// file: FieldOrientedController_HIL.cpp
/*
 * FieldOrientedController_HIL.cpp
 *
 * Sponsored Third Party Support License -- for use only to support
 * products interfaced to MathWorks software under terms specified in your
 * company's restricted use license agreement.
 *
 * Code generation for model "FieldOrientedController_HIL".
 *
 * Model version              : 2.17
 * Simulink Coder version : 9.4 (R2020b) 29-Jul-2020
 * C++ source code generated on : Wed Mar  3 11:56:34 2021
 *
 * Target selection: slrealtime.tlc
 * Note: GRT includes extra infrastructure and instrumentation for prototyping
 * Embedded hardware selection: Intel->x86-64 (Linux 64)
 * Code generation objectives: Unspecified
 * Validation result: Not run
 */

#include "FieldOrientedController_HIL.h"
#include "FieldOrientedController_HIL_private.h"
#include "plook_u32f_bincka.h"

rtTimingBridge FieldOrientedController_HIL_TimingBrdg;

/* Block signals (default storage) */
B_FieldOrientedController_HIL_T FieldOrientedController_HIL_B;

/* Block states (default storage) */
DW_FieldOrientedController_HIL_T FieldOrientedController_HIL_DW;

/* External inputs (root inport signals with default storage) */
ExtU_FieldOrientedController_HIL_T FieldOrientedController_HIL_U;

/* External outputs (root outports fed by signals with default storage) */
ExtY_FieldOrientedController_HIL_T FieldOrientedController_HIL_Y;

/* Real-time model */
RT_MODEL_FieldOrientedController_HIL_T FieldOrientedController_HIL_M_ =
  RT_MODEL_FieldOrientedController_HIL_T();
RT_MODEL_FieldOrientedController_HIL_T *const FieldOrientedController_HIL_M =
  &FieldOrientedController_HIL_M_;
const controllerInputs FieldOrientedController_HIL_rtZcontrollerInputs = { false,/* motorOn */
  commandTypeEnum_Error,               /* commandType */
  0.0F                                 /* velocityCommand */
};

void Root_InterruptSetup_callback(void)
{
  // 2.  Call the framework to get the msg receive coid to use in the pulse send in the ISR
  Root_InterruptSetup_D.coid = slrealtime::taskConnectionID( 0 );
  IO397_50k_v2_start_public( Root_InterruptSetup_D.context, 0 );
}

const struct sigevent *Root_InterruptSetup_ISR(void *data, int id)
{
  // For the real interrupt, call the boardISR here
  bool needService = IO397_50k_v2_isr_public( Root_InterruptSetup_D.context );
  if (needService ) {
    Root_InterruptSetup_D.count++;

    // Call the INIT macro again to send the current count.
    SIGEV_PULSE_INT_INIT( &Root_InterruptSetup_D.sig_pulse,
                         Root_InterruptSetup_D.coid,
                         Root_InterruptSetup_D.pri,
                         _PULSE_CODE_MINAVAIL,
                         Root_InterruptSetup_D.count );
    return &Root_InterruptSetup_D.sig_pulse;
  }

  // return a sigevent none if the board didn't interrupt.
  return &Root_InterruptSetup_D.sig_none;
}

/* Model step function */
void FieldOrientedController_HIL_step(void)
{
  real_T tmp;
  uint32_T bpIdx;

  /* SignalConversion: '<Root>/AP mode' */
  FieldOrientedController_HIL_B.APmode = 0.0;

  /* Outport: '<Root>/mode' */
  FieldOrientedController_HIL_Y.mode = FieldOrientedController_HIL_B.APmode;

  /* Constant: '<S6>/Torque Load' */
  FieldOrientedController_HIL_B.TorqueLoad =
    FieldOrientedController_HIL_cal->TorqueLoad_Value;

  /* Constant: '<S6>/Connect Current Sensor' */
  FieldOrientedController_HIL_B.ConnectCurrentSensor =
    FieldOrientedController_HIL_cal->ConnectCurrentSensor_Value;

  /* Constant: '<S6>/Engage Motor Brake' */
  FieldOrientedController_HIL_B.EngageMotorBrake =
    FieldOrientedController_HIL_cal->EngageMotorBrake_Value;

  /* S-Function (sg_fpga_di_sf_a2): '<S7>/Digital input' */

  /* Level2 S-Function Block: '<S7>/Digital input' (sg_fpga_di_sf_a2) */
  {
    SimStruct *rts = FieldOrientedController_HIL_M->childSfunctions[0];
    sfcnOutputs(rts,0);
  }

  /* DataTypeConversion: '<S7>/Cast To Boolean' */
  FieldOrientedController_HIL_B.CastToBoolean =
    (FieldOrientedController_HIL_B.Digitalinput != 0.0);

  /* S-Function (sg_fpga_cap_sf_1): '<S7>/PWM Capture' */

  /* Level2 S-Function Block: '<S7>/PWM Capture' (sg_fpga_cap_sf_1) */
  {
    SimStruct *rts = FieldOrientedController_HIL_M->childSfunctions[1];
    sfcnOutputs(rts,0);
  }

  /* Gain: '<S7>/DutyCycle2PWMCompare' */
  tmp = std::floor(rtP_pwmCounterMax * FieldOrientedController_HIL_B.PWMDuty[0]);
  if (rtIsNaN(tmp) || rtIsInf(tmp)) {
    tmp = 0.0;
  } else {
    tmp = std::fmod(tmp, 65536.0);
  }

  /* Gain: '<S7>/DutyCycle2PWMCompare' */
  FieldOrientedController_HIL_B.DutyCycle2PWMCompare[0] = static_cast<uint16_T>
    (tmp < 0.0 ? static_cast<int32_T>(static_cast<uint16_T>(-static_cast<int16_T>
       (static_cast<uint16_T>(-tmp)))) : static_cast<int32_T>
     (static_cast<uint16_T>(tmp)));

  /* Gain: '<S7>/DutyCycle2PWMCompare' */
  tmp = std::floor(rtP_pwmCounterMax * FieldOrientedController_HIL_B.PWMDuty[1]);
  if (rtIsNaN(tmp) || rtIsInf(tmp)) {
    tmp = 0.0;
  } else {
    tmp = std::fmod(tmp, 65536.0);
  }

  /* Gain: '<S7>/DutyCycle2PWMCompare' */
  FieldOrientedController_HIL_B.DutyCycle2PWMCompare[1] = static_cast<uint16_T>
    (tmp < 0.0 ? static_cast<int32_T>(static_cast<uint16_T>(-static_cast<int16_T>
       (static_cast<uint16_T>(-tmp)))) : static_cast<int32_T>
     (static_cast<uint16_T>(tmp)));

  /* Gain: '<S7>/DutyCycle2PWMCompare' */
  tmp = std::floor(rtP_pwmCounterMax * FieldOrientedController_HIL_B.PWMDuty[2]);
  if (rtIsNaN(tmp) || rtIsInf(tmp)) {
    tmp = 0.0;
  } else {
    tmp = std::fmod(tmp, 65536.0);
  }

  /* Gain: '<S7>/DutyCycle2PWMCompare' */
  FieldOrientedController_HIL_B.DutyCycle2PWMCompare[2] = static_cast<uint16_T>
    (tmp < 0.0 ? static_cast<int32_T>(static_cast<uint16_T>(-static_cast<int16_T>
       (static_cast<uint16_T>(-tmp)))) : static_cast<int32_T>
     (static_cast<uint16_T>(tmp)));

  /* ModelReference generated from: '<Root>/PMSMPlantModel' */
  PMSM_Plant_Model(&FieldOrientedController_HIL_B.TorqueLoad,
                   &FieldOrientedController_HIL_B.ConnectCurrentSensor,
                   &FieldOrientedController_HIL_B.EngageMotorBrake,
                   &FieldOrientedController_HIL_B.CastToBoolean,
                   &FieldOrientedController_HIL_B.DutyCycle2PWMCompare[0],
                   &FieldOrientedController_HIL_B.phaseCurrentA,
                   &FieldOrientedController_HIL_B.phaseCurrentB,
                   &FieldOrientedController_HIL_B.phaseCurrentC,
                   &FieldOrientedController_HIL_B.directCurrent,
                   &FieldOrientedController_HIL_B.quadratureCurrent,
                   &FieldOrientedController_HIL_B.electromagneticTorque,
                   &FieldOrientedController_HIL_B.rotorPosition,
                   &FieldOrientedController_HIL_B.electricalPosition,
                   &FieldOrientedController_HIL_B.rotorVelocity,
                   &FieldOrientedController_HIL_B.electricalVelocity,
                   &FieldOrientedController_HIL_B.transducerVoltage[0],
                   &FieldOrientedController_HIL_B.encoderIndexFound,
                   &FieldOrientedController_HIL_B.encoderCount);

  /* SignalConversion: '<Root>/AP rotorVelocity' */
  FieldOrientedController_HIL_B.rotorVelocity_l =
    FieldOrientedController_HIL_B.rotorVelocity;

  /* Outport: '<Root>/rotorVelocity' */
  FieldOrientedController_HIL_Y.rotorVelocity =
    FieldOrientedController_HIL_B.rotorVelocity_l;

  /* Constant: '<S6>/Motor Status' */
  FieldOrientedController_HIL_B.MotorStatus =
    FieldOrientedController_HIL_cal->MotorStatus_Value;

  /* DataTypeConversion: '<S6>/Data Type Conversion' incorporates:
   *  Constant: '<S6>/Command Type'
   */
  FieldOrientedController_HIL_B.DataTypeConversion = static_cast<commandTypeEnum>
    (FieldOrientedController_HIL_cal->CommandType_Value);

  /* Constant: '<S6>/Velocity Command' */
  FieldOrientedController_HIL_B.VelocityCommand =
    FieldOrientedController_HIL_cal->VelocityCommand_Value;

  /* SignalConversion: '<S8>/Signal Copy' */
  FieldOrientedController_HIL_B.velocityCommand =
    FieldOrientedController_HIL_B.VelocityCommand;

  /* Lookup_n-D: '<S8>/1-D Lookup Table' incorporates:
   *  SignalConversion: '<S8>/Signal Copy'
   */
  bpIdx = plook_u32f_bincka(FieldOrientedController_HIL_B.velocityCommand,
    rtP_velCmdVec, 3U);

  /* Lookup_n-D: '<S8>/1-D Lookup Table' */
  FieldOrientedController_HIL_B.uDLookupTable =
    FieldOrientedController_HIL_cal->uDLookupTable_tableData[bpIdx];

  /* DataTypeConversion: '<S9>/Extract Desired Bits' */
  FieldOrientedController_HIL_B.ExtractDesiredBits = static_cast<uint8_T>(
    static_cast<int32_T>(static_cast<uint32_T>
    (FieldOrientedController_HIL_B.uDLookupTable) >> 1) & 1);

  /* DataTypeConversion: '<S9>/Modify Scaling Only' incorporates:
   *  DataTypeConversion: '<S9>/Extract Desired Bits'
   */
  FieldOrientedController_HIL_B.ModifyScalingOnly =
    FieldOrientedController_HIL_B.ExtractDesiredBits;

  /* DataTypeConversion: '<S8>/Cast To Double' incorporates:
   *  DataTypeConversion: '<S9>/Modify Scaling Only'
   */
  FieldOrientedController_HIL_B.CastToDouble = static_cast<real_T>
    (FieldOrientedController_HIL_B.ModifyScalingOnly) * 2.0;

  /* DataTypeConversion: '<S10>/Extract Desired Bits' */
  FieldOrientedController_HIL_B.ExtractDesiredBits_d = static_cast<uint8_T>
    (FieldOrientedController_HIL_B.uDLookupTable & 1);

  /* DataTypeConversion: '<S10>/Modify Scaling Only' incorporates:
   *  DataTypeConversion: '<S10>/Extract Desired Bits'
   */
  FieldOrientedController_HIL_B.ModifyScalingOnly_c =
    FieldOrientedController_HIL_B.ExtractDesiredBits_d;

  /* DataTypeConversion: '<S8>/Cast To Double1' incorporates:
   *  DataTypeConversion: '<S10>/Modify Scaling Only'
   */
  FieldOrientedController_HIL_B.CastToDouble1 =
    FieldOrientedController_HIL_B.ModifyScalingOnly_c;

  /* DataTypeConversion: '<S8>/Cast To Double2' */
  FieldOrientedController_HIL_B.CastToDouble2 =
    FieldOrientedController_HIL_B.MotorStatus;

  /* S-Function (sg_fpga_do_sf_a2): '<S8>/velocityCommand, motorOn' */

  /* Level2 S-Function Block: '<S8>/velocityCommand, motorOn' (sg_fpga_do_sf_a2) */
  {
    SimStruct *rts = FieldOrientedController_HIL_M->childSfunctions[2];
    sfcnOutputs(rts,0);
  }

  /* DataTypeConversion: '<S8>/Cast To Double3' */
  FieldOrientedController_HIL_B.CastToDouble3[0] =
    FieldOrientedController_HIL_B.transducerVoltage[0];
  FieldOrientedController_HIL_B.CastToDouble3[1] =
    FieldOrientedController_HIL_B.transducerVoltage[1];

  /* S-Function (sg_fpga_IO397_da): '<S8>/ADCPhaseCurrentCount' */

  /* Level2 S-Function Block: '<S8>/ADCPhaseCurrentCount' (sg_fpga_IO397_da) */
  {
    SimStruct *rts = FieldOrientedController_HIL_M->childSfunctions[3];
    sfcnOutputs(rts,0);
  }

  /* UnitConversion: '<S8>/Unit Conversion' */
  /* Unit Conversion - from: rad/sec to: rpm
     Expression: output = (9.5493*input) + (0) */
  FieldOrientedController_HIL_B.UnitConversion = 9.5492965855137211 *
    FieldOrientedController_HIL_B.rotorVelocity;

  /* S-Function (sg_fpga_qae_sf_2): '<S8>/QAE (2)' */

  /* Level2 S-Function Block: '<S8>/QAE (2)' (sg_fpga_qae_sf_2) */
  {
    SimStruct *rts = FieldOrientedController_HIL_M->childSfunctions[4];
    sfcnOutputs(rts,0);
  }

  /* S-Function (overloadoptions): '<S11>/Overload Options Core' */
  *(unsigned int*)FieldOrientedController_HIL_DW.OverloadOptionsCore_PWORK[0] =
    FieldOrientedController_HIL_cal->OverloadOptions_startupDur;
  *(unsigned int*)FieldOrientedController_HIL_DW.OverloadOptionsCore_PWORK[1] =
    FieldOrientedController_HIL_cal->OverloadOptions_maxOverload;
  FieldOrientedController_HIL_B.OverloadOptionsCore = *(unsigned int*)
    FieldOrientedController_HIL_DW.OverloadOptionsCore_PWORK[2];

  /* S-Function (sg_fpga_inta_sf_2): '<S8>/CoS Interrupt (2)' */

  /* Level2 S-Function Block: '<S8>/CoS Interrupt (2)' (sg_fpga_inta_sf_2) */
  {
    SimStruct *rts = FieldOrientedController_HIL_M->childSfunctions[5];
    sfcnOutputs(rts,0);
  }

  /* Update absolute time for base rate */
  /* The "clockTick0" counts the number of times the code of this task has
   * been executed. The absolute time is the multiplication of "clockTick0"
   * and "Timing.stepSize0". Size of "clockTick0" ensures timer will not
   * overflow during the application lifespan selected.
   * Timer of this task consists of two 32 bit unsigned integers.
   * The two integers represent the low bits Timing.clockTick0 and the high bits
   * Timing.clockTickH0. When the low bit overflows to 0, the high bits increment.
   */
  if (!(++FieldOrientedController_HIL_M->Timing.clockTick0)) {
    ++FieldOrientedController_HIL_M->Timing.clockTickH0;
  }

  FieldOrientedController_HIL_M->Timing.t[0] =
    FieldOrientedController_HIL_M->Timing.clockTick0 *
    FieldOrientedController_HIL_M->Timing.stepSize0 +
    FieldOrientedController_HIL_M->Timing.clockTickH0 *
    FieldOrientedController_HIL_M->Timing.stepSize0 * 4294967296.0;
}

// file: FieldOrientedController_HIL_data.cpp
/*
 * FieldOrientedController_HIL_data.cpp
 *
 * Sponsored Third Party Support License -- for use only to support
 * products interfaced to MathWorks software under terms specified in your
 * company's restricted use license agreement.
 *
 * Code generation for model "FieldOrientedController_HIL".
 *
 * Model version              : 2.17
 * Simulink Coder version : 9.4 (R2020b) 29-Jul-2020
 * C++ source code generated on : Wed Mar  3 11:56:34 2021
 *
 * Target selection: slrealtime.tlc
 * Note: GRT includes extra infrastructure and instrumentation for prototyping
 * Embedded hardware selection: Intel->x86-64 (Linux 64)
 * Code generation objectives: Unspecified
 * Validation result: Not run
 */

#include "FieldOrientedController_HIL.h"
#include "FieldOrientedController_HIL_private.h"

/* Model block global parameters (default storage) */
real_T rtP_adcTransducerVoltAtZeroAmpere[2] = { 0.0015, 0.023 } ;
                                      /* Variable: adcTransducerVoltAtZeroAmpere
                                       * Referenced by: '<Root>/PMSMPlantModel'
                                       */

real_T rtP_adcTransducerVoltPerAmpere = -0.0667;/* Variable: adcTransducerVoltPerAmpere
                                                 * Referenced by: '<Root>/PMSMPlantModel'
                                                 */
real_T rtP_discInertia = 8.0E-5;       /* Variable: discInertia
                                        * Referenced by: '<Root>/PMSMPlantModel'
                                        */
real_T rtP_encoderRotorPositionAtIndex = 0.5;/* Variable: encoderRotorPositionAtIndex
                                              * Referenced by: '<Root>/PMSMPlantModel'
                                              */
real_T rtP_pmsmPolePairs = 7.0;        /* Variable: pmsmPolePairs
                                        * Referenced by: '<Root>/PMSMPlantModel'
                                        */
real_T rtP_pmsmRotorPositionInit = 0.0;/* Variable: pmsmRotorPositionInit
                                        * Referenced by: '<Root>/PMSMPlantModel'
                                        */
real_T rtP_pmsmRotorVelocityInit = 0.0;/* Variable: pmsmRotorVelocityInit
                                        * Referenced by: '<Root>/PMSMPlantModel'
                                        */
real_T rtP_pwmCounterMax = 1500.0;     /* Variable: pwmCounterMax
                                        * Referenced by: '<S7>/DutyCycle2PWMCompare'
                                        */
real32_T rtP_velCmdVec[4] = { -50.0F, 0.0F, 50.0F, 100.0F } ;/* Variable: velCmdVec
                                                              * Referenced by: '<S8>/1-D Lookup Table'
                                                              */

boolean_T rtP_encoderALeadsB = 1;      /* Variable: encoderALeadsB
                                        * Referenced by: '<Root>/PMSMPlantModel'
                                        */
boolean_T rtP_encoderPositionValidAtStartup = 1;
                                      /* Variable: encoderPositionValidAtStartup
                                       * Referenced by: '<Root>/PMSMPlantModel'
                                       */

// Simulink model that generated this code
simulink model "FieldOrientedController_HIL"  (R2020b)
settings: configuration reference "SLRT_HIL" (kept outside this file)
undefined symbols (not defined in the file): encoderNumberOfSlits, idxVec, IO397, modeSchedulerEnum, pwmCounterMax, sampleTimeCurrentControl, velCmdVec
libraries: utils_lib x2, speedgoatlib_fpga_dio x2, simulink x2, SignalEditorBlockLib x1, speedgoatlib_interrupt x1, speedgoatlib_fpga_pwm x1, speedgoatlib_fpga_analog_io x1, speedgoatlib_fpga_inta x1, slrealtimetgmanagement x1, speedgoatlib_fpga_quadrature x1, speedgoatlib_fpga x1

== system FieldOrientedController_HIL ==
  note: Electric Motor Control
      | Reference application model
      | © 2007 - 2020 Speedgoat GmbH
  physicalInputs : Inport  OutDataTypeStr=Bus: physicalInputs
  controllerInputs : Inport  Port=2  OutDataTypeStr=Bus: controllerInputs
  ADC : utils_lib/ADC  SystemSampleTime=-1  VariantActivationTime=update diagram  Latency=0  AutoFrameSizeCalculation=off
  AP mode : SignalConversion  OverrideOpt=off
  AP rotorVelocity : SignalConversion  OverrideOpt=off
  Bus Selector : BusSelector  OutputSignals=rotorVelocity
  DAC : utils_lib/DAC  SystemSampleTime=-1  VariantActivationTime=update diagram  Latency=0  AutoFrameSizeCalculation=off
  Inputs : Subsystem  Variant=on  VariantControlMode=label  VariantControl=Choice  LabelModeActiveChoice=dashboardInput
  Interrupt Setup : speedgoatlib_interrupt/Interrupt Setup  parModuleTrigger=on  parPollingMode=off  parPriorityConf=High  parPriority=241  confStartFcn=IO397_50k_v2_start_public  confStopFcn=IO397_50k_v2_stop_public  confIsrFcn=IO397_50k_v2_isr_public  confMapFcn=IO397_50k_v2_map_public  confHookFile=io397_50k_v2_int_hooks.c  confIrqNr=-1  confIsMdlTrig=on  confIsPolling=off  confPriority=254  confModID=1  confSelectedInt=Speedgoat IO397-50k v2 interrupt  confSelectedId=1
  PMSMPlantModel : ModelReference  ModelNameDialog=PMSM_Plant_Model  SimulationMode=Normal  ModelReferenceVersion=2.0
  Signal Copy : SignalConversion  OverrideOpt=off
  Signal Copy1 : SignalConversion  OverrideOpt=off
  TIC2000 : Subsystem  VariantControl=demoMode == 3
  UserInterface : Subsystem
  mode : Outport
  rotorVelocity : Outport  Port=2
  tag scope: rotorVelocity=global
  wires:
  ADC/2 -> TIC2000/2(controllerFeedback)
  PMSMPlantModel/1 -> Bus Selector/1  "motorMeasurements"
  ADC/1 -> TIC2000/1(controllerInputs)
  TIC2000/2(" controllerCommands") -> DAC/1  "motorCommands"
  DAC/1 -> PMSMPlantModel/2
  Bus Selector/1 -> [rotorVelocity], AP rotorVelocity/1  "<rotorVelocity>"
  Inputs/2(controllerInputs) -> ADC/1  "controllerInputs"
  physicalInputs/1 -> Signal Copy/1
  controllerInputs/1 -> Signal Copy1/1
  Inputs/1(physicalInputs) -> PMSMPlantModel/1  "physicalInputs"
  AP rotorVelocity/1 -> rotorVelocity/1  "rotorVelocity"
  TIC2000/1(mode) -> AP mode/1
  AP mode/1 -> mode/1
  PMSMPlantModel/2 -> ADC/2  "controllerFeedback"
  Signal Copy/1 -> Inputs/1(physicalInputs_in)
  Signal Copy1/1 -> Inputs/2(controllerInputs_in)

== system FieldOrientedController_HIL/Inputs ==
  physicalInputs_in : Inport  OutDataTypeStr=Bus: physicalInputs
  controllerInputs_in : Inport  Port=2  OutDataTypeStr=Bus: controllerInputs
  Dashboard : Subsystem  VariantControl=dashboardInput
  Harness : Subsystem  VariantControl=harnessInput
  Signal Builder : Subsystem  VariantControl=sigBuilderInput
  physicalInputs : Outport  OutDataTypeStr=Bus: physicalInputs
  controllerInputs : Outport  Port=2  OutDataTypeStr=Bus: controllerInputs

== system FieldOrientedController_HIL/TIC2000 ==
  note: TI C2000 Controller
  controllerInputs : Inport
  controllerFeedback : Inport  Port=2
  Speedgoat_inputs : Subsystem
  Speedgoat_outputs : Subsystem
  mode : Outport
  " controllerCommands" : Outport  Port=2  VectorParamsAs1DForOutWhenUnconnected=off
  wires:
  Speedgoat_inputs/2(commands) -> " controllerCommands"/1
  Speedgoat_inputs/1(mode) -> mode/1
  controllerFeedback/1 -> Speedgoat_outputs/2(feedback)
  controllerInputs/1 -> Speedgoat_outputs/1(inputs)

== system FieldOrientedController_HIL/UserInterface ==
  Dashboard Scope : DashboardScope  TimeSpan=10  Ymin=-200  Ymax=200  ScaleAtStop=off
  Half Gauge : SemiCircularGaugeBlock  ScaleMin=-200  ScaleMax=200
  Rotary Switch : RotarySwitchBlock
  Toggle Switch : ToggleSwitchBlock

== system FieldOrientedController_HIL/Inputs/Dashboard ==
  Command Type : Constant  Value=3  OutDataTypeStr=uint8
  Connect Current Sensor : Constant  OutDataTypeStr=boolean
  Data Type Conversion : DataTypeConversion  OutDataTypeStr=Enum: commandTypeEnum
  Engage Motor Brake : Constant  Value=0  OutDataTypeStr=boolean
  Motor Status : Constant  OutDataTypeStr=boolean
  Torque Load : Constant  Value=0  OutDataTypeStr=Inherit: Inherit via back propagation
  Velocity Command : Constant  Value=100  OutDataTypeStr=Inherit: Inherit via back propagation
  Bus Element Out : Outport  PortName=physicalInputs  Element=torqueLoad
  Bus Element Out1 : Outport  PortName=physicalInputs  Element=connectCurrentSensor
  Bus Element Out2 : Outport  PortName=physicalInputs  Element=motorBrake
  Bus Element Out3 : Outport  Port=2  PortName=controllerInputs  Element=motorOn
  Bus Element Out4 : Outport  Port=2  PortName=controllerInputs  Element=commandType
  Bus Element Out5 : Outport  Port=2  PortName=controllerInputs  Element=velocityCommand
  wires:
  Engage Motor Brake/1 -> Bus Element Out2/1
  Data Type Conversion/1 -> Bus Element Out4/1
  Connect Current Sensor/1 -> Bus Element Out1/1
  Torque Load/1 -> Bus Element Out/1
  Velocity Command/1 -> Bus Element Out5/1
  Command Type/1 -> Data Type Conversion/1
  Motor Status/1 -> Bus Element Out3/1

== system FieldOrientedController_HIL/Inputs/Harness ==
  physicalInputs_in : Inport  OutDataTypeStr=Bus: physicalInputs
  controllerInputs_in : Inport  Port=2  OutDataTypeStr=Bus: controllerInputs
  physicalInputs : Outport  OutDataTypeStr=Bus: physicalInputs
  controllerInputs : Outport  Port=2  OutDataTypeStr=Bus: controllerInputs
  wires:
  physicalInputs_in/1 -> physicalInputs/1
  controllerInputs_in/1 -> controllerInputs/1

== system FieldOrientedController_HIL/Inputs/Signal Builder ==
  Signal Editor : SignalEditorBlockLib/Signal Editor  FileName=systemInputs.mat  ActiveScenario=doubleStepPosNegClosedLoop  ActiveSignal=controlInputs  IsBus=on  OutputBusObjectStr=Bus: controllerInputs  SampleTime=-1  Interpolate=off  ZeroCross=off  OutputAfterFinalValue=Holding final value  Unit=inherit  PreserveSignalName=on
  physicalInputs : Outport  OutDataTypeStr=Bus: physicalInputs
  controllerInputs : Outport  Port=2  OutDataTypeStr=Bus: controllerInputs
  wires:
  Signal Editor/1 -> physicalInputs/1
  Signal Editor/2 -> controllerInputs/1

== system FieldOrientedController_HIL/TIC2000/Speedgoat_inputs ==
  Cast To Boolean : DataTypeConversion  OutDataTypeStr=boolean
  Constant : Constant  Commented=on  Value=modeSchedulerEnum(0)
  Digital input : speedgoatlib_fpga_dio/Digital input  id=1  chan=[2]  ts=sampleTimeCurrentControl  pciSlot=-1  board=IO397-50k  vectorizeOutput=off
  DutyCycle2PWMCompare : Gain  Gain=pwmCounterMax  OutDataTypeStr=Inherit: Inherit via back propagation
  PWM Capture : speedgoatlib_fpga_pwm/PWM Capture  id=1  chan=[1 2 3]  ts=sampleTimeCurrentControl  pciSlot=-1  board=IO397-50k  captureMode=High transitions triggered  captureTimeout=0  bit_width_cap=24  showHighDuration=off  showLowDuration=off  showPeriod=off  showDC16=on  showDC8=off  showTOn=off  showTOff=off  showValidData=off
  mode : Outport
  Bus Element Out : Outport  Port=2  PortName=commands  Element=inverterEnable
  Bus Element Out1 : Outport  Port=2  PortName=commands  Element=pwmCompare
  wires:
  PWM Capture/1 -> DutyCycle2PWMCompare/1  "PWMDuty"
  Digital input/1 -> Cast To Boolean/1
  DutyCycle2PWMCompare/1 -> Bus Element Out1/1
  Cast To Boolean/1 -> Bus Element Out/1
  Constant/1 -> mode/1

== system FieldOrientedController_HIL/TIC2000/Speedgoat_outputs ==
  Bus Element In1 : Inport  PortName=inputs  Element=motorOn
  Bus Element In : Inport  PortName=inputs  Element=velocityCommand
  Bus Element In2 : Inport  Port=2  PortName=feedback  Element=transducerVoltage
  1-D Lookup Table : Lookup_n-D  NumberOfTableDimensions=1  BreakpointsForDimension1=velCmdVec  Table=idxVec  InterpMethod=Flat  InternalRulePriority=Speed  OutDataTypeStr=uint8  RndMeth=Simplest  InputSameDT=on
  ADCPhaseCurrentCount : speedgoatlib_fpga_analog_io/IO397 Analog Output  id=1  chan=1:2  initVal=0  resetVal=1  ts=-1  pciSlot=-1  board=IO397-50k  span=+-5 V
  Cast To Double{,1..3} (4 alike) : DataTypeConversion  OutDataTypeStr=double
  CoS Interrupt (2) : speedgoatlib_fpga_inta/CoS Interrupt (2)  id=1  channel=[1]  pciSlot=-1  ts=-1  board=IO397-50k  fpga_frequency=0  int_source=internally generated  mode=0  debounce=0  delay=0  ad_settings=off  division=0  multiplication=0  gap=1e-3  int_freq=1/sampleTimeCurrentControl  freq_2_time=2.50000e-04  event=off  timestamp=off  flag=off
  Demux : Demux  Outputs=2
  Extract Bits : simulink/Logic and Bit Operations/Extract Bits  bitsToExtract=Range of bits  numBits=8  bitIdxRange=1  outScalingMode=Preserve fixed-point scaling
  Extract Bits1 : simulink/Logic and Bit Operations/Extract Bits  bitsToExtract=Range of bits  numBits=8  bitIdxRange=0  outScalingMode=Preserve fixed-point scaling
  Overload Options : slrealtimetgmanagement/Overload Options  startupDur=10  startupDurSrc=Tunable Parameter  maxOverload=10  maxOverloadSrc=Tunable Parameter  TETFlag=off
  QAE (2) : speedgoatlib_fpga_quadrature/QAE (2)  id=1  channel=1  ts=-1  pciSlot=-1  board=IO397-50k  numSeg=encoderNumberOfSlits*2  phaseAngle=90  initSpeed=0  initPos=pmsmRotorPositionInit  freeWheel=on  showInputSpeed=on  showInputPosition=off  showOutputPosition=off
  Setup : speedgoatlib_fpga/Setup/Setup  board=IO397-50k  id=1  device_id=1  frontIO=None  rearIO=None  bitstreamFile=speedgoat_IO397_50k_CI_02168  rev=1.0  timestamp_string=26/08/20 11:01:36  fpgaFreq=75 MHz  fpgaTick=13.33 ns  ProgSpiFlash=off  ProgBPIFlash=off  pciSlot=-1  PullRPort0=pull-up 3.3V  VioPort0=3.3V  PullRPort1=pull-up 3.3V  VioPort1=3.3V  PullRPort2=pull-up 3.3V  VioPort2=3.3V  PullRPort3=pull-up 3.3V  VioPort3=3.3V  PullRPort4=pull-up 3.3V  VioPort4=3.3V  PullRPort5=pull-up 3.3V  VioPort5=3.3V  PullRPort6=pull-up 3.3V  VioPort6=3.3V  PullRPort15=pull-up 3.3V  PullRPort31=pull-up 3.3V  PullRPort47=pull-up 3.3V  PullRPort63=pull-up 3.3V
  Signal Copy : SignalConversion  OverrideOpt=off
  Signal Specification : SignalSpecification  Unit=rpm
  Unit Conversion : UnitConversion
  "velocityCommand, motorOn" : speedgoatlib_fpga_dio/Digital output  id=1  chan=[3,4,1]  init=0  reset=1  vectorizeInput=off  ts=-1  pciSlot=-1  board=IO397-50k
  wires:
  Demux/2 -> ADCPhaseCurrentCount/2
  Demux/1 -> ADCPhaseCurrentCount/1
  1-D Lookup Table/1 -> Extract Bits1/1, Extract Bits/1
  Bus Element In1/1 -> Cast To Double2/1
  Cast To Double/1 -> "velocityCommand, motorOn"/1
  Cast To Double1/1 -> "velocityCommand, motorOn"/2
  Extract Bits/1 -> Cast To Double/1
  Extract Bits1/1 -> Cast To Double1/1
  Unit Conversion/1 -> Signal Specification/1
  Cast To Double2/1 -> "velocityCommand, motorOn"/3
  Cast To Double3/1 -> Demux/1
  Bus Element In/1 -> Signal Copy/1
  [rotorVelocity] -> Unit Conversion/1
  Signal Specification/1 -> QAE (2)/1
  Bus Element In2/1 -> Cast To Double3/1
  Signal Copy/1 -> 1-D Lookup Table/1  "velocityCommand"
